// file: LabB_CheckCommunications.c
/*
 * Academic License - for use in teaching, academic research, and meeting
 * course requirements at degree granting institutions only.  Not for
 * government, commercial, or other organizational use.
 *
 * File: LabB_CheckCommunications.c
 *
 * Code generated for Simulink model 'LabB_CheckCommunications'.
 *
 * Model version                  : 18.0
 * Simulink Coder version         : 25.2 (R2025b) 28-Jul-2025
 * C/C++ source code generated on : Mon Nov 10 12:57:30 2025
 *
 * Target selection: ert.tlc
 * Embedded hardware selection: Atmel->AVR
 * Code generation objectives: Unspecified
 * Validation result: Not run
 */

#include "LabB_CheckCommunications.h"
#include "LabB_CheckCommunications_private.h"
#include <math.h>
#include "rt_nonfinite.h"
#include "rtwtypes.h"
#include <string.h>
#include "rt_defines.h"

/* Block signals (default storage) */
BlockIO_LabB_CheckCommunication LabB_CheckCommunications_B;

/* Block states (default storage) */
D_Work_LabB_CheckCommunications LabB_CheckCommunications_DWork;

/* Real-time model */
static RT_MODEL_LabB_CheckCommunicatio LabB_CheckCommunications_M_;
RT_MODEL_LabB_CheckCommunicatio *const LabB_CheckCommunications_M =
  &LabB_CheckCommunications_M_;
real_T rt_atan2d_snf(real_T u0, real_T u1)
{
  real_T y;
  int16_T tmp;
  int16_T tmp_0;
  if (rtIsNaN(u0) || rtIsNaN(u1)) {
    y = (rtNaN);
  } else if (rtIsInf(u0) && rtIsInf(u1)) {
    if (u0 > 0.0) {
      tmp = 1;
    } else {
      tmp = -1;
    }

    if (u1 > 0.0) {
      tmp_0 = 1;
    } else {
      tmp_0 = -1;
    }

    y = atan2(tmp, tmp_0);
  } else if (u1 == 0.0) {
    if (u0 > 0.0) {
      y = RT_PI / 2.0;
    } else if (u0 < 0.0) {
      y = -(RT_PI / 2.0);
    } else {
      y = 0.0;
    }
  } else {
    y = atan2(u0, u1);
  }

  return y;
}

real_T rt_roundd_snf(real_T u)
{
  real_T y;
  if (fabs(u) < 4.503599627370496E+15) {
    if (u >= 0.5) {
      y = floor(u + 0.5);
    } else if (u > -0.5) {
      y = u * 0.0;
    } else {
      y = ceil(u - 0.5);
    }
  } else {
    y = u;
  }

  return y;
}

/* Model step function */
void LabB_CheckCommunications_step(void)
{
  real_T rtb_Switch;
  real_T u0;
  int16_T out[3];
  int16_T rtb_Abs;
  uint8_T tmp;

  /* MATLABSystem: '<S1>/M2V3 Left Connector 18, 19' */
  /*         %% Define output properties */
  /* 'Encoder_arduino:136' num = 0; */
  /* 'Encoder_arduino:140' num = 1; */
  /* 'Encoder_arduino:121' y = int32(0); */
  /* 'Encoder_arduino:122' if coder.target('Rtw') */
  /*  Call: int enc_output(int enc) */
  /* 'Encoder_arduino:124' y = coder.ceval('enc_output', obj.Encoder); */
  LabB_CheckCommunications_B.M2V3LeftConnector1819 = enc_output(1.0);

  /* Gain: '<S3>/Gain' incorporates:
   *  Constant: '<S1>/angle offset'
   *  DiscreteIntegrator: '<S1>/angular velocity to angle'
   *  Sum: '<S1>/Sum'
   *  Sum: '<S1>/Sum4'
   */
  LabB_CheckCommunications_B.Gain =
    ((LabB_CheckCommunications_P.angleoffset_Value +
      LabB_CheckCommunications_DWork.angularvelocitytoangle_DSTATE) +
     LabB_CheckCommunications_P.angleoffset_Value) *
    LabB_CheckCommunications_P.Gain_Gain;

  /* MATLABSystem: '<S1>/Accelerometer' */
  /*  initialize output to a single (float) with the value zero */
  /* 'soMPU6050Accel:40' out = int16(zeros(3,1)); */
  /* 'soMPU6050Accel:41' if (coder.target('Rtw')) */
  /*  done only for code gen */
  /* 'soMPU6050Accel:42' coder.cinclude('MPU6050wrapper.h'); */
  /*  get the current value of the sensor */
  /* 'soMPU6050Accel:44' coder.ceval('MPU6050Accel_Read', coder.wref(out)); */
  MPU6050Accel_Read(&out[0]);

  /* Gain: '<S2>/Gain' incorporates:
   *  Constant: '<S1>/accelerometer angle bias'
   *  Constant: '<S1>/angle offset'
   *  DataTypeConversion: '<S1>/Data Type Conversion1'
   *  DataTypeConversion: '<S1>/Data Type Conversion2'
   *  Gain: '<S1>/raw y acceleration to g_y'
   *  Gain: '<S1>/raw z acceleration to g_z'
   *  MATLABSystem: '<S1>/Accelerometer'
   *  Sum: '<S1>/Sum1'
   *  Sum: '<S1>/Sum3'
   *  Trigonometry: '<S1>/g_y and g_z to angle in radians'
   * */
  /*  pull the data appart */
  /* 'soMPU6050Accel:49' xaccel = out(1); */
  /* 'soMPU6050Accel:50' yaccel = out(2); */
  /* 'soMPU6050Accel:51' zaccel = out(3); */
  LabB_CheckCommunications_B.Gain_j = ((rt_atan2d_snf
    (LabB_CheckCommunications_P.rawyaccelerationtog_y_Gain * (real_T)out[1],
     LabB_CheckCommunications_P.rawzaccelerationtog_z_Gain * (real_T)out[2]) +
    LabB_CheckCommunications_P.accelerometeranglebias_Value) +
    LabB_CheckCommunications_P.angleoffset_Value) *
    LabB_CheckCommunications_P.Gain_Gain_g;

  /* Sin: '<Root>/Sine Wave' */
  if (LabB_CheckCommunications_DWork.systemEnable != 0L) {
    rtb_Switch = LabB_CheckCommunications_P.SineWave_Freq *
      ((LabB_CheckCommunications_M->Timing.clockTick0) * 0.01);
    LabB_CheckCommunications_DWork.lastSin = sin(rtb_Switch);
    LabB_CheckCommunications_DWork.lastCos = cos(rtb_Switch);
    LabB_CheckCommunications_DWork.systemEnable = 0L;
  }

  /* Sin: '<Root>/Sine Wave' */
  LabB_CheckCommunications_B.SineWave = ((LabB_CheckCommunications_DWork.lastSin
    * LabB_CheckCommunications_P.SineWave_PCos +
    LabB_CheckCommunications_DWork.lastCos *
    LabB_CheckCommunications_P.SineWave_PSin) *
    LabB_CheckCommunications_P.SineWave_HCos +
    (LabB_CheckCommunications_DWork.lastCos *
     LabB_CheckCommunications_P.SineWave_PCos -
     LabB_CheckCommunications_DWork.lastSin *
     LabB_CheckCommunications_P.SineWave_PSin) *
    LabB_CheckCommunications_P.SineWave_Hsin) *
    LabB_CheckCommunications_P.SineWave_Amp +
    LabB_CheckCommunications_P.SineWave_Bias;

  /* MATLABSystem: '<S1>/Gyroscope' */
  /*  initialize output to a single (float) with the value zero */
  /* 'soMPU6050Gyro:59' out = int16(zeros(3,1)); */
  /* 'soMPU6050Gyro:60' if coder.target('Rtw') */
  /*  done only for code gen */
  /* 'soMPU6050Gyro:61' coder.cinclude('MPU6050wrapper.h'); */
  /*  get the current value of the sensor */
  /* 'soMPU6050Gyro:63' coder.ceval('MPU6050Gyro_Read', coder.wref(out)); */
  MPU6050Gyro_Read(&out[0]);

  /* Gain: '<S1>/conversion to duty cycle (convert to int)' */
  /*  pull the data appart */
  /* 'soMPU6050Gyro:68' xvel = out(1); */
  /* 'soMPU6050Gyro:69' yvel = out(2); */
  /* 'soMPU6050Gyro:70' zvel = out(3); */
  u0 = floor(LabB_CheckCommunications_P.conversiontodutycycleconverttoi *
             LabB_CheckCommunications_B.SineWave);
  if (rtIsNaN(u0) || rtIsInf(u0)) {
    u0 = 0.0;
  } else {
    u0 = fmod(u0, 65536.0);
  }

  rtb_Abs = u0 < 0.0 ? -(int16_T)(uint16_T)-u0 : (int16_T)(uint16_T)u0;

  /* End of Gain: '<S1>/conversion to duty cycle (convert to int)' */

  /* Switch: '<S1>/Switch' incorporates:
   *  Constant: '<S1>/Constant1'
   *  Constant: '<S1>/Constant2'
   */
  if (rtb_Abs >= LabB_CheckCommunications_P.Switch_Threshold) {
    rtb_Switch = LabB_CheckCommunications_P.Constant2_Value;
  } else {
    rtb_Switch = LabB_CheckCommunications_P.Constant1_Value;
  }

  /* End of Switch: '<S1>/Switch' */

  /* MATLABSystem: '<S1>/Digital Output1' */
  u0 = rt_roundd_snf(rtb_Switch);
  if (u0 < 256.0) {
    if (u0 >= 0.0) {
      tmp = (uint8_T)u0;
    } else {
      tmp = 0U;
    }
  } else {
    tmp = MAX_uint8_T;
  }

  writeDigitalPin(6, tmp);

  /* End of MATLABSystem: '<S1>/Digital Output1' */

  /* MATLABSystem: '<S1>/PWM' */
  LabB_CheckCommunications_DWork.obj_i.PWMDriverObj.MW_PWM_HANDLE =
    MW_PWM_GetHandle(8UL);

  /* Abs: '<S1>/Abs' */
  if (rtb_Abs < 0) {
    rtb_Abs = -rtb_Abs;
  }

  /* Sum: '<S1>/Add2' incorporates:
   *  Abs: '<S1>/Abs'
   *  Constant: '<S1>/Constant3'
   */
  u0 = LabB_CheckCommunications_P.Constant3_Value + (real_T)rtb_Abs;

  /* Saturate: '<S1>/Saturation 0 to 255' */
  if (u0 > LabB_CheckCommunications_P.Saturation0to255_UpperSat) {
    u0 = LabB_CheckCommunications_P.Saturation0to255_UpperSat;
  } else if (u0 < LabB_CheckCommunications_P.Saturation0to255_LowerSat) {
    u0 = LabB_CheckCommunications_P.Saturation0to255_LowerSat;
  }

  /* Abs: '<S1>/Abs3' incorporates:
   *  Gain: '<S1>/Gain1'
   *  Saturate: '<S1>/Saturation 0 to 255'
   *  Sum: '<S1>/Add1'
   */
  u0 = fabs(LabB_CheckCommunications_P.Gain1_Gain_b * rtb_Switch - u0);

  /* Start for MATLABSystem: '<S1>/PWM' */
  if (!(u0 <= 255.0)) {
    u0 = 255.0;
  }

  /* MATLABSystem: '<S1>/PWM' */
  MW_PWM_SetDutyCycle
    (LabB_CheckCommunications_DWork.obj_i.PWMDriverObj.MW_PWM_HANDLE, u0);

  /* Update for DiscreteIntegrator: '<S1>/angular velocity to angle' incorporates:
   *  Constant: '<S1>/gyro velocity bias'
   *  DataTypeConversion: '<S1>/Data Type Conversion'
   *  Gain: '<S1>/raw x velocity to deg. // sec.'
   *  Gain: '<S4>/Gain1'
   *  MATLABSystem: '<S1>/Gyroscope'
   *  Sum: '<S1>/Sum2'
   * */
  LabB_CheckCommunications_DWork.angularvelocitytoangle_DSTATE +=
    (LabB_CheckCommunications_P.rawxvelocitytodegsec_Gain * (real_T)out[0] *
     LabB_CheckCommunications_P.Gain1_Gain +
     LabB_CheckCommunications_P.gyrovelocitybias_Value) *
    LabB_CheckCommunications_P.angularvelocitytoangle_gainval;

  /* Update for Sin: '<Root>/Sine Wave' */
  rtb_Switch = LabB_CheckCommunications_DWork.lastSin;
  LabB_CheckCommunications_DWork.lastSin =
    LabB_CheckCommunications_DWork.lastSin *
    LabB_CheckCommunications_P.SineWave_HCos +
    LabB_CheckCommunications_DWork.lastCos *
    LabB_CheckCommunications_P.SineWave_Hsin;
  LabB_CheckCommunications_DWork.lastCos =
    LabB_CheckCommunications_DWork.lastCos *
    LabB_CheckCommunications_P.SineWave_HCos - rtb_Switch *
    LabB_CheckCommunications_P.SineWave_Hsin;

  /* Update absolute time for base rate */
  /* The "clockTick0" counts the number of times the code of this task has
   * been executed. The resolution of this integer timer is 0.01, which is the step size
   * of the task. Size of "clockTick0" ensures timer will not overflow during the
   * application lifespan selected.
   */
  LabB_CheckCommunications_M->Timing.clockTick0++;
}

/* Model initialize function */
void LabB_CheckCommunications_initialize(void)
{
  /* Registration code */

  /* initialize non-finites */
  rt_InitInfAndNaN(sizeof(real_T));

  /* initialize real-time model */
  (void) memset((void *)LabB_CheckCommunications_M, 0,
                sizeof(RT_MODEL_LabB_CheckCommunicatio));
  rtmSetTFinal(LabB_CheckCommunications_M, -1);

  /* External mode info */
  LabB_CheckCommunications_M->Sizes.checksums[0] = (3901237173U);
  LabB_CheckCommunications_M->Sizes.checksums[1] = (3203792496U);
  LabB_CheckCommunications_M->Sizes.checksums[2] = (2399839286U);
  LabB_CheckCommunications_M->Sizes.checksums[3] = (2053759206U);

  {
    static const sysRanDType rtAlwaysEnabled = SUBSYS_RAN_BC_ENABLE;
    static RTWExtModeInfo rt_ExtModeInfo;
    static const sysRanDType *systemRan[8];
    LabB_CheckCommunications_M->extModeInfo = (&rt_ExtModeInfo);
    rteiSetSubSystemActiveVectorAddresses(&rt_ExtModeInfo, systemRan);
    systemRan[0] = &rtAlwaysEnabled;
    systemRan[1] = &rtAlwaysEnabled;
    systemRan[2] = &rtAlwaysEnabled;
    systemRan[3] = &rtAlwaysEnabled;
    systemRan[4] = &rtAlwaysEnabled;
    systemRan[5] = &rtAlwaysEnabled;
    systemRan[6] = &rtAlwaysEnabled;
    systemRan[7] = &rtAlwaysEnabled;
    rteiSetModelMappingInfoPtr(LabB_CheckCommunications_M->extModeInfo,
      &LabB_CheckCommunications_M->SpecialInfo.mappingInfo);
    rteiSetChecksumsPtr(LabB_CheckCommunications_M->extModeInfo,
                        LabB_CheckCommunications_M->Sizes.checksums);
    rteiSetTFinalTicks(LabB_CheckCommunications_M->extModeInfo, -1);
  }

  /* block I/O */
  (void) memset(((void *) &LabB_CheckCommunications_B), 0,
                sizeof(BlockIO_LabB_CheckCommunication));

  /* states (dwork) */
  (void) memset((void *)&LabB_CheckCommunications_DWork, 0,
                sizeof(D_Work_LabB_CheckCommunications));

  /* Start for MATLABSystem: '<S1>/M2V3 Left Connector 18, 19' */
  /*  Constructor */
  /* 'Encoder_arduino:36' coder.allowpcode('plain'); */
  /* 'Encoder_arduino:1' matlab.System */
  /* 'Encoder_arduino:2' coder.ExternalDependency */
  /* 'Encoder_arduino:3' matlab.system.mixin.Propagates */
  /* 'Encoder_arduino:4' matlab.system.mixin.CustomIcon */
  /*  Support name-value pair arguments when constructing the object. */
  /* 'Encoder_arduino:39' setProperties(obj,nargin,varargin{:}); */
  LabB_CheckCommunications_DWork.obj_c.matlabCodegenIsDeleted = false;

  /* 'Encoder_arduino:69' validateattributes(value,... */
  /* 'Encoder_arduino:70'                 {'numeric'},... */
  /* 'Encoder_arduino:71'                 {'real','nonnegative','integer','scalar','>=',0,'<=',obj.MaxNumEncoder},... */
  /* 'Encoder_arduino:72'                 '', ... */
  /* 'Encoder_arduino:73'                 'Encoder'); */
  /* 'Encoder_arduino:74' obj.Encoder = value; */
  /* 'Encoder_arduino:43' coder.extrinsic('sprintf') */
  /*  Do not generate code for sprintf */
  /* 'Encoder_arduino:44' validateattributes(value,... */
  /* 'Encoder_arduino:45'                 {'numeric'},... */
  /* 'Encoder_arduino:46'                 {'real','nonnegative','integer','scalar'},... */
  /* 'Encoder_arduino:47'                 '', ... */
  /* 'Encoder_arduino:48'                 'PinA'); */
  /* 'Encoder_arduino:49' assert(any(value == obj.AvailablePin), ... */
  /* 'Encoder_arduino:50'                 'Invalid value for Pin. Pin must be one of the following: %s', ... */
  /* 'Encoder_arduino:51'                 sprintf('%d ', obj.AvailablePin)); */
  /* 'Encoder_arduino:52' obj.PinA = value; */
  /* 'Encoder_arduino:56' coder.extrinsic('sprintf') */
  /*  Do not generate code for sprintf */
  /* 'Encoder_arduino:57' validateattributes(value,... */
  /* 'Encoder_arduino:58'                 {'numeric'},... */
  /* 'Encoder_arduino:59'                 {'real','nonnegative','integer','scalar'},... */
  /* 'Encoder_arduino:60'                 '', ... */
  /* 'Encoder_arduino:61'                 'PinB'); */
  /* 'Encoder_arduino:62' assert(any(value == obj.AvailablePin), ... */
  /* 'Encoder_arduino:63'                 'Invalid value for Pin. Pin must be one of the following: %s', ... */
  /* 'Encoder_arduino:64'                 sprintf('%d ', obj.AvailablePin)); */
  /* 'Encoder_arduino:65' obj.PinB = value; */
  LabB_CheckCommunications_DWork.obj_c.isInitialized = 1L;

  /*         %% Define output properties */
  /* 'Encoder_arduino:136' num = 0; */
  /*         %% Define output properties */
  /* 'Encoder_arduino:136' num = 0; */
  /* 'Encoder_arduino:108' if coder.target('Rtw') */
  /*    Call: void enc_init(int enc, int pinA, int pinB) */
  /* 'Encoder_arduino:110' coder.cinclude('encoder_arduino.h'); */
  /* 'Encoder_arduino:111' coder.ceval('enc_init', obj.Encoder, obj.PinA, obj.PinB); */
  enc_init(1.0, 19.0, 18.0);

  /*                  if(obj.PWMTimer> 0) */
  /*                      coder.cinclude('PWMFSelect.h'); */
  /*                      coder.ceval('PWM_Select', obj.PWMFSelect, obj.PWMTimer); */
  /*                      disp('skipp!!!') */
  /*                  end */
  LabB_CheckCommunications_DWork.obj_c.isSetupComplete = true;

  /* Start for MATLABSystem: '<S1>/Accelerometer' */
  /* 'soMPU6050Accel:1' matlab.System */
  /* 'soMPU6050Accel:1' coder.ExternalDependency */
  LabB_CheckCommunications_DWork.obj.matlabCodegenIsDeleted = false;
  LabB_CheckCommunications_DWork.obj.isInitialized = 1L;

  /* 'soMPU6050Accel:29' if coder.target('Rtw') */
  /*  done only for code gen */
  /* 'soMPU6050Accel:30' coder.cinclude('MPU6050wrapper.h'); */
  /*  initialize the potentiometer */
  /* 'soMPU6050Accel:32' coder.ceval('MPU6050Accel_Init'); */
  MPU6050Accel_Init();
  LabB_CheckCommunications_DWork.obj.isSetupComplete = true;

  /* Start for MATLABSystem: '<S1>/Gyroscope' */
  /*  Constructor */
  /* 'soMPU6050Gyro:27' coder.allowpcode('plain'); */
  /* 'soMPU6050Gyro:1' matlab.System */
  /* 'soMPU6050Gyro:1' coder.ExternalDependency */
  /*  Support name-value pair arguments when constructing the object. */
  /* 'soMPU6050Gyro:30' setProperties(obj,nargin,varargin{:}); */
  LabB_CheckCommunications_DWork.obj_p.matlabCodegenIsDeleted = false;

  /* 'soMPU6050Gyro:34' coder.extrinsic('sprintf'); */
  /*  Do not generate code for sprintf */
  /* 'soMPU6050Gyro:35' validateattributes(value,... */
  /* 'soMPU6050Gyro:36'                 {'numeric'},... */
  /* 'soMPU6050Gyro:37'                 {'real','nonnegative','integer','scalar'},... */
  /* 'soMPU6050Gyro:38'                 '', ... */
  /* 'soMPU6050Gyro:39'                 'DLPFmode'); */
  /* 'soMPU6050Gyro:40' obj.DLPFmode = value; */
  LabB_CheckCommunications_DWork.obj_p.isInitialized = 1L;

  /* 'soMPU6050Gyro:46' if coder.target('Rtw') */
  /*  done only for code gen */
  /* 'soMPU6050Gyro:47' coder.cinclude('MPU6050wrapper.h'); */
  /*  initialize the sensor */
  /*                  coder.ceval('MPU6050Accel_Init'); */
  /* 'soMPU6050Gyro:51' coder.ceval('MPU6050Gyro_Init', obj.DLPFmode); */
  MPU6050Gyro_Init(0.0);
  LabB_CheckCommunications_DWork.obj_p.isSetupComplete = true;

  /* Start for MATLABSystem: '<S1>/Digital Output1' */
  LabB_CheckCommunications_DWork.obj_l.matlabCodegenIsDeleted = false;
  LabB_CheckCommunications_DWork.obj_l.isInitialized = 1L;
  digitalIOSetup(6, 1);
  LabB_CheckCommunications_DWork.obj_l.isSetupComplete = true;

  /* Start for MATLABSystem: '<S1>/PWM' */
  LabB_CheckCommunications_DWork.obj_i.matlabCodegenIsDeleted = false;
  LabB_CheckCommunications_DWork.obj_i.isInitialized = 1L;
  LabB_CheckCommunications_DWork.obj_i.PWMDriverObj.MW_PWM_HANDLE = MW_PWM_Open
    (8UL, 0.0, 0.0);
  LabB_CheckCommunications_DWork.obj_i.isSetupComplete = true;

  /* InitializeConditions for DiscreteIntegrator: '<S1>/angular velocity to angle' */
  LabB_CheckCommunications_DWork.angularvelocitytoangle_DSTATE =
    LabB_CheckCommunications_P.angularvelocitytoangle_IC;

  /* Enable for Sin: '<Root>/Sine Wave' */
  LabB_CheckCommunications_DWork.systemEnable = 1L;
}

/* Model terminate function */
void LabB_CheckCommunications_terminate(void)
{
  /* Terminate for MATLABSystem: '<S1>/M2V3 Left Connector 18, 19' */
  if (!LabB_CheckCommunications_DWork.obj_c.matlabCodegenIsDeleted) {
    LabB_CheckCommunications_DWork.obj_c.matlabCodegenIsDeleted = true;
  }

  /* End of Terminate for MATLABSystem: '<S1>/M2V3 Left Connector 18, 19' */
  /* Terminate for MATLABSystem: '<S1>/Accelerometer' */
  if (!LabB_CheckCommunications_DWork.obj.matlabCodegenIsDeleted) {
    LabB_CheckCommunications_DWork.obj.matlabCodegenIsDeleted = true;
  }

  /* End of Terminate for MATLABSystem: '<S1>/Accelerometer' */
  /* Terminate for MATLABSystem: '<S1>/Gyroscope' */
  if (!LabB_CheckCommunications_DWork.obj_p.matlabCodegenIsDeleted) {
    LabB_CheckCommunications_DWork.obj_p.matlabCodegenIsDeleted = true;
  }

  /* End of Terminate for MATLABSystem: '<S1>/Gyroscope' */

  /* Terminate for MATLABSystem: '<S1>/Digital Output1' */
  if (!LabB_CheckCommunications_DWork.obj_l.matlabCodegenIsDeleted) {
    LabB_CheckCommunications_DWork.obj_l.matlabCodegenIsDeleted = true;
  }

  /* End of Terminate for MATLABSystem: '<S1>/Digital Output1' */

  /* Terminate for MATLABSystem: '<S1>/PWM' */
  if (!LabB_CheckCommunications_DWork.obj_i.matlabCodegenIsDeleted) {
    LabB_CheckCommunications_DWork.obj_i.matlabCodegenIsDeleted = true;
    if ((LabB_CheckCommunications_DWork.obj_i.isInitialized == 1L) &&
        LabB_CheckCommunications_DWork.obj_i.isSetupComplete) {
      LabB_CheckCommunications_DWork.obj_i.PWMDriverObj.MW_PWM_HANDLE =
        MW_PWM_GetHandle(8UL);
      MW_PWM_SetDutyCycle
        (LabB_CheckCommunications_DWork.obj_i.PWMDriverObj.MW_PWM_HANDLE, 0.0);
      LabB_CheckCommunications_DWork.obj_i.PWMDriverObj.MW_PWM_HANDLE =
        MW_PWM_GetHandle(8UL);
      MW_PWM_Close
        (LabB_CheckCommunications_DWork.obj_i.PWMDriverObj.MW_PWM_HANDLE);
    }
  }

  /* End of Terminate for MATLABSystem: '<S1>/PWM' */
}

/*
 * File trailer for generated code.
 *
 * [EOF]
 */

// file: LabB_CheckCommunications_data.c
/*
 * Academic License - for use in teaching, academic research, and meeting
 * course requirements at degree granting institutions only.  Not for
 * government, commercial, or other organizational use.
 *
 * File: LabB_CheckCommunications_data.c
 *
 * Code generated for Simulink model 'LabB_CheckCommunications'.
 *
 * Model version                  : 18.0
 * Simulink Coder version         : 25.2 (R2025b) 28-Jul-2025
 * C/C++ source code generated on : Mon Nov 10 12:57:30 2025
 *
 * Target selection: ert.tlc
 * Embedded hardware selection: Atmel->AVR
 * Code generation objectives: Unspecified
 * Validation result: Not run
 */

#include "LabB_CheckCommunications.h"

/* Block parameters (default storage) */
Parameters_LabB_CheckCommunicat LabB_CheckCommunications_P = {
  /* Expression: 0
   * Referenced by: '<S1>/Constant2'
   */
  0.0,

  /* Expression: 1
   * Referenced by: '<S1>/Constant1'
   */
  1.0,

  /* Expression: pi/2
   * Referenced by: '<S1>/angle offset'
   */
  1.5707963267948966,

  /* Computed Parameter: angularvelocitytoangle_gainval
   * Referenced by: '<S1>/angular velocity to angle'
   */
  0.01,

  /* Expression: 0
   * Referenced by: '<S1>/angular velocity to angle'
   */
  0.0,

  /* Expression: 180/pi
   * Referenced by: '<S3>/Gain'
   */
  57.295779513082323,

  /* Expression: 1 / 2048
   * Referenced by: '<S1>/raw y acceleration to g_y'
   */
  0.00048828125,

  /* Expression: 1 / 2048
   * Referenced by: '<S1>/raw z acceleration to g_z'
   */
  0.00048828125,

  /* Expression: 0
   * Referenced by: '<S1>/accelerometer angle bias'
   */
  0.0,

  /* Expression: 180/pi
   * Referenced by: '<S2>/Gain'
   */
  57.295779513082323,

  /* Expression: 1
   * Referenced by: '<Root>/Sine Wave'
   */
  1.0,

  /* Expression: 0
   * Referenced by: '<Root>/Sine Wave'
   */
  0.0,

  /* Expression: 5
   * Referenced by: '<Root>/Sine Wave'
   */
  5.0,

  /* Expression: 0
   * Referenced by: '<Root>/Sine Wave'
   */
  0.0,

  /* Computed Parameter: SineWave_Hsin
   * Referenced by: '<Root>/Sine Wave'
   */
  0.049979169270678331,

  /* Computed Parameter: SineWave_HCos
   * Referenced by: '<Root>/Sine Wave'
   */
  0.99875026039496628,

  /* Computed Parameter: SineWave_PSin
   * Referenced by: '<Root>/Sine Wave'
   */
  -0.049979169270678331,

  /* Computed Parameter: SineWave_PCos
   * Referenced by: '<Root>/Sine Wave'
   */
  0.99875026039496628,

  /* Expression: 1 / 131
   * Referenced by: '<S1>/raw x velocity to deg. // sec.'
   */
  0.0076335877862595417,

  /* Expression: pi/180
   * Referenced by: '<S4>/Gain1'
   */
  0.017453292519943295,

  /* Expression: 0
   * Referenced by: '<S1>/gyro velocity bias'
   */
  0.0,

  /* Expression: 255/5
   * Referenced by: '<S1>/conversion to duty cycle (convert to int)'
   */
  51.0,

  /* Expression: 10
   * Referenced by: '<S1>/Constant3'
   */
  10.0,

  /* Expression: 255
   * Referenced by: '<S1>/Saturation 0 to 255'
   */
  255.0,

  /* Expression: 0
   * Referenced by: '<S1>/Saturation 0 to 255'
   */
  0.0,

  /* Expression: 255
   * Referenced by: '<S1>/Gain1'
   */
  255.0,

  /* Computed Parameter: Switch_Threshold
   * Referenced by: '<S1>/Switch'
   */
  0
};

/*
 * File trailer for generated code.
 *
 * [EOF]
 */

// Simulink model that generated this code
simulink model "LabB_CheckCommunications"  (R2025b)
settings: Solver=FixedStepDiscrete  StartTime=0.0  StopTime=Inf  FixedStep=fSamplingPeriod  RelTol=1e-3  EnableMultiTasking=on
values from neighbouring files (symbols this model uses):
  fSamplingPeriod = 0.01    [GetDataFromSerial.m]    (also in GetRuns.m = 0.005; LabA_Solutions_LoadPhysicalParameters.m = 1 / sampling_freq; LabA_solutions.m = 1 / sampling_freq; LabB_ObserverAndControllerOverRobot_Parameters.m = 0.005)
undefined symbols (not defined in the file or in its folder): DiscIntNeverNeededParam
libraries: simulink_extras x3, arduinolib x3, xpcutilitieslib x1, MinSegLibrary_M2V3 x1

== system LabB_CheckCommunications ==
  note: load parameters
  Balancing Robot : Subsystem
  Radians to Degrees : simulink_extras/Transformations/Radians to Degrees
  Radians to Degrees1 : simulink_extras/Transformations/Radians to Degrees
  Sine Wave : Sin  Frequency=5  SampleTime=fSamplingPeriod
  accelerometer : Scope
  encoder : Scope
  gyro : Scope
  motor : Scope
  wires:
  Balancing Robot/1(angle from gyroscope in radians) -> Radians to Degrees1/1
  Balancing Robot/2(angle from accelerometer in radians) -> Radians to Degrees/1
  Balancing Robot/3(encoder) -> encoder/1
  Radians to Degrees1/1 -> gyro/1
  Radians to Degrees/1 -> accelerometer/1
  Sine Wave/1 -> motor/1, Balancing Robot/1(volt)

== system LabB_CheckCommunications/Balancing Robot ==
  note: v_m
  note: direction
  note: Encoder
  note: Accelerometer and gyro
  note: Motor
  note: Serial communications
  note: x_w
  note: x_vel
  note: y_acc
  note: z_acc
  volt : Inport
  Abs : Abs  SaturateOnIntegerOverflow=off
  Abs3 : Abs  SaturateOnIntegerOverflow=off
  Accelerometer : MATLABSystem  System=soMPU6050Accel  SimulateUsing=Code generation
  Add1 : Sum  Inputs=-+
  Add2 : Sum
  "Byte Packing " : xpcutilitieslib/Byte Packing   Commented=on  MaskPackedDataType=uint8  MaskUnpackedDataTypes={'single','double','double','double','double'}  MaskAlignment=1
  Constant1 : Constant
  Constant2 : Constant  Value=0
  Constant3 : Constant  Value=10
  Data Type Conversion : DataTypeConversion  OutDataTypeStr=double  SaturateOnIntegerOverflow=off  RndMeth=Floor
  Data Type Conversion1 : DataTypeConversion  OutDataTypeStr=double  SaturateOnIntegerOverflow=off  RndMeth=Floor
  Data Type Conversion2 : DataTypeConversion  OutDataTypeStr=double  SaturateOnIntegerOverflow=off  RndMeth=Floor
  Data Type Conversion3 : DataTypeConversion  Commented=on  OutDataTypeStr=single  SaturateOnIntegerOverflow=off  RndMeth=Floor
  Data Type Conversion5 : DataTypeConversion  Commented=on  OutDataTypeStr=double  SaturateOnIntegerOverflow=off  RndMeth=Floor
  Degrees to Radians : simulink_extras/Transformations/Degrees to Radians
  Digital Output1 : arduinolib/Digital Output  pinNumber=6  Direction=output  blockPlatform=arduino
  Gain1 : Gain  Gain=255
  Gyroscope : MATLABSystem  System=soMPU6050Gyro  DLPFmode=0
  "M2V3 Left Connector 18, 19" : MinSegLibrary_M2V3/M2V3 Left Connector 18, 19  Encoder=1  PinA=19  PinB=18
  PWM : arduinolib/PWM  pinNumber=8  frequencyType=Default  desiredFrequency=490.2  achievableFrequency=490.2
  Saturation 0 to 255 : Saturate  UpperLimit=255  LowerLimit=0
  Serial Transmit : arduinolib/Serial Transmit  Commented=on  portNumber=0  sendmode=write  sendformat=Decimal  floatprecision=2  blockPlatform=arduino
  Sum{,1..2,4} (4 alike) : Sum  Inputs=++|
  Sum3 : Sum  Inputs=|++
  Switch : Switch  SaturateOnIntegerOverflow=off  InputSameDT=off
  accelerometer angle bias : Constant  Value=0
  angle offset : Constant  Value=pi/2
  angular velocity to angle : DiscreteIntegrator  SampleTime=-1  ICPrevOutput=DiscIntNeverNeededParam  ICPrevScaledInput=DiscIntNeverNeededParam
  conversion to duty cycle (convert to int) : Gain  Gain=255/5  OutDataTypeStr=int16
  g_y and g_z to angle in radians : Trigonometry  Operator=atan2
  gyro velocity bias : Constant  Value=0
  raw x velocity to deg. / sec. : Gain  Gain=1 / 131
  raw y acceleration to g_y : Gain  Gain=1 / 2048
  raw z acceleration to g_z : Gain  Gain=1 / 2048
  angle from gyroscope in radians : Outport
  angle from accelerometer in radians : Outport  Port=2
  encoder : Outport  Port=3
  wires:
  Gyroscope/1 -> Data Type Conversion/1
  Accelerometer/2 -> Data Type Conversion1/1
  raw z acceleration to g_z/1 -> g_y and g_z to angle in radians/2
  raw y acceleration to g_y/1 -> g_y and g_z to angle in radians/1
  angle offset/1 -> Sum4/1, Sum1/1, Sum/1
  raw x velocity to deg. / sec./1 -> Degrees to Radians/1
  Sum/1 -> Sum4/2
  Data Type Conversion2/1 -> "Byte Packing "/5, raw z acceleration to g_z/1
  Data Type Conversion1/1 -> "Byte Packing "/4, raw y acceleration to g_y/1
  Data Type Conversion/1 -> "Byte Packing "/3, raw x velocity to deg. / sec./1
  Accelerometer/3 -> Data Type Conversion2/1
  Add2/1 -> Saturation 0 to 255/1
  Abs/1 -> Add2/2
  Constant3/1 -> Add2/1
  Abs3/1 -> PWM/1
  Saturation 0 to 255/1 -> Add1/1
  conversion to duty cycle (convert to int)/1 -> Abs/1, Switch/2
  Add1/1 -> Abs3/1
  Gain1/1 -> Add1/2
  Constant1/1 -> Switch/3
  Constant2/1 -> Switch/1
  Switch/1 -> Gain1/1, Digital Output1/1
  volt/1 -> Data Type Conversion3/1, conversion to duty cycle (convert to int)/1
  "Byte Packing "/1 -> Serial Transmit/1
  "M2V3 Left Connector 18, 19"/1 -> encoder/1, Data Type Conversion5/1
  Data Type Conversion3/1 -> "Byte Packing "/1
  Data Type Conversion5/1 -> "Byte Packing "/2
  Sum1/1 -> angle from accelerometer in radians/1
  angular velocity to angle/1 -> Sum/2
  Degrees to Radians/1 -> Sum2/2
  gyro velocity bias/1 -> Sum2/1
  Sum2/1 -> angular velocity to angle/1
  g_y and g_z to angle in radians/1 -> Sum3/1
  Sum3/1 -> Sum1/2
  accelerometer angle bias/1 -> Sum3/2
  Sum4/1 -> angle from gyroscope in radians/1
